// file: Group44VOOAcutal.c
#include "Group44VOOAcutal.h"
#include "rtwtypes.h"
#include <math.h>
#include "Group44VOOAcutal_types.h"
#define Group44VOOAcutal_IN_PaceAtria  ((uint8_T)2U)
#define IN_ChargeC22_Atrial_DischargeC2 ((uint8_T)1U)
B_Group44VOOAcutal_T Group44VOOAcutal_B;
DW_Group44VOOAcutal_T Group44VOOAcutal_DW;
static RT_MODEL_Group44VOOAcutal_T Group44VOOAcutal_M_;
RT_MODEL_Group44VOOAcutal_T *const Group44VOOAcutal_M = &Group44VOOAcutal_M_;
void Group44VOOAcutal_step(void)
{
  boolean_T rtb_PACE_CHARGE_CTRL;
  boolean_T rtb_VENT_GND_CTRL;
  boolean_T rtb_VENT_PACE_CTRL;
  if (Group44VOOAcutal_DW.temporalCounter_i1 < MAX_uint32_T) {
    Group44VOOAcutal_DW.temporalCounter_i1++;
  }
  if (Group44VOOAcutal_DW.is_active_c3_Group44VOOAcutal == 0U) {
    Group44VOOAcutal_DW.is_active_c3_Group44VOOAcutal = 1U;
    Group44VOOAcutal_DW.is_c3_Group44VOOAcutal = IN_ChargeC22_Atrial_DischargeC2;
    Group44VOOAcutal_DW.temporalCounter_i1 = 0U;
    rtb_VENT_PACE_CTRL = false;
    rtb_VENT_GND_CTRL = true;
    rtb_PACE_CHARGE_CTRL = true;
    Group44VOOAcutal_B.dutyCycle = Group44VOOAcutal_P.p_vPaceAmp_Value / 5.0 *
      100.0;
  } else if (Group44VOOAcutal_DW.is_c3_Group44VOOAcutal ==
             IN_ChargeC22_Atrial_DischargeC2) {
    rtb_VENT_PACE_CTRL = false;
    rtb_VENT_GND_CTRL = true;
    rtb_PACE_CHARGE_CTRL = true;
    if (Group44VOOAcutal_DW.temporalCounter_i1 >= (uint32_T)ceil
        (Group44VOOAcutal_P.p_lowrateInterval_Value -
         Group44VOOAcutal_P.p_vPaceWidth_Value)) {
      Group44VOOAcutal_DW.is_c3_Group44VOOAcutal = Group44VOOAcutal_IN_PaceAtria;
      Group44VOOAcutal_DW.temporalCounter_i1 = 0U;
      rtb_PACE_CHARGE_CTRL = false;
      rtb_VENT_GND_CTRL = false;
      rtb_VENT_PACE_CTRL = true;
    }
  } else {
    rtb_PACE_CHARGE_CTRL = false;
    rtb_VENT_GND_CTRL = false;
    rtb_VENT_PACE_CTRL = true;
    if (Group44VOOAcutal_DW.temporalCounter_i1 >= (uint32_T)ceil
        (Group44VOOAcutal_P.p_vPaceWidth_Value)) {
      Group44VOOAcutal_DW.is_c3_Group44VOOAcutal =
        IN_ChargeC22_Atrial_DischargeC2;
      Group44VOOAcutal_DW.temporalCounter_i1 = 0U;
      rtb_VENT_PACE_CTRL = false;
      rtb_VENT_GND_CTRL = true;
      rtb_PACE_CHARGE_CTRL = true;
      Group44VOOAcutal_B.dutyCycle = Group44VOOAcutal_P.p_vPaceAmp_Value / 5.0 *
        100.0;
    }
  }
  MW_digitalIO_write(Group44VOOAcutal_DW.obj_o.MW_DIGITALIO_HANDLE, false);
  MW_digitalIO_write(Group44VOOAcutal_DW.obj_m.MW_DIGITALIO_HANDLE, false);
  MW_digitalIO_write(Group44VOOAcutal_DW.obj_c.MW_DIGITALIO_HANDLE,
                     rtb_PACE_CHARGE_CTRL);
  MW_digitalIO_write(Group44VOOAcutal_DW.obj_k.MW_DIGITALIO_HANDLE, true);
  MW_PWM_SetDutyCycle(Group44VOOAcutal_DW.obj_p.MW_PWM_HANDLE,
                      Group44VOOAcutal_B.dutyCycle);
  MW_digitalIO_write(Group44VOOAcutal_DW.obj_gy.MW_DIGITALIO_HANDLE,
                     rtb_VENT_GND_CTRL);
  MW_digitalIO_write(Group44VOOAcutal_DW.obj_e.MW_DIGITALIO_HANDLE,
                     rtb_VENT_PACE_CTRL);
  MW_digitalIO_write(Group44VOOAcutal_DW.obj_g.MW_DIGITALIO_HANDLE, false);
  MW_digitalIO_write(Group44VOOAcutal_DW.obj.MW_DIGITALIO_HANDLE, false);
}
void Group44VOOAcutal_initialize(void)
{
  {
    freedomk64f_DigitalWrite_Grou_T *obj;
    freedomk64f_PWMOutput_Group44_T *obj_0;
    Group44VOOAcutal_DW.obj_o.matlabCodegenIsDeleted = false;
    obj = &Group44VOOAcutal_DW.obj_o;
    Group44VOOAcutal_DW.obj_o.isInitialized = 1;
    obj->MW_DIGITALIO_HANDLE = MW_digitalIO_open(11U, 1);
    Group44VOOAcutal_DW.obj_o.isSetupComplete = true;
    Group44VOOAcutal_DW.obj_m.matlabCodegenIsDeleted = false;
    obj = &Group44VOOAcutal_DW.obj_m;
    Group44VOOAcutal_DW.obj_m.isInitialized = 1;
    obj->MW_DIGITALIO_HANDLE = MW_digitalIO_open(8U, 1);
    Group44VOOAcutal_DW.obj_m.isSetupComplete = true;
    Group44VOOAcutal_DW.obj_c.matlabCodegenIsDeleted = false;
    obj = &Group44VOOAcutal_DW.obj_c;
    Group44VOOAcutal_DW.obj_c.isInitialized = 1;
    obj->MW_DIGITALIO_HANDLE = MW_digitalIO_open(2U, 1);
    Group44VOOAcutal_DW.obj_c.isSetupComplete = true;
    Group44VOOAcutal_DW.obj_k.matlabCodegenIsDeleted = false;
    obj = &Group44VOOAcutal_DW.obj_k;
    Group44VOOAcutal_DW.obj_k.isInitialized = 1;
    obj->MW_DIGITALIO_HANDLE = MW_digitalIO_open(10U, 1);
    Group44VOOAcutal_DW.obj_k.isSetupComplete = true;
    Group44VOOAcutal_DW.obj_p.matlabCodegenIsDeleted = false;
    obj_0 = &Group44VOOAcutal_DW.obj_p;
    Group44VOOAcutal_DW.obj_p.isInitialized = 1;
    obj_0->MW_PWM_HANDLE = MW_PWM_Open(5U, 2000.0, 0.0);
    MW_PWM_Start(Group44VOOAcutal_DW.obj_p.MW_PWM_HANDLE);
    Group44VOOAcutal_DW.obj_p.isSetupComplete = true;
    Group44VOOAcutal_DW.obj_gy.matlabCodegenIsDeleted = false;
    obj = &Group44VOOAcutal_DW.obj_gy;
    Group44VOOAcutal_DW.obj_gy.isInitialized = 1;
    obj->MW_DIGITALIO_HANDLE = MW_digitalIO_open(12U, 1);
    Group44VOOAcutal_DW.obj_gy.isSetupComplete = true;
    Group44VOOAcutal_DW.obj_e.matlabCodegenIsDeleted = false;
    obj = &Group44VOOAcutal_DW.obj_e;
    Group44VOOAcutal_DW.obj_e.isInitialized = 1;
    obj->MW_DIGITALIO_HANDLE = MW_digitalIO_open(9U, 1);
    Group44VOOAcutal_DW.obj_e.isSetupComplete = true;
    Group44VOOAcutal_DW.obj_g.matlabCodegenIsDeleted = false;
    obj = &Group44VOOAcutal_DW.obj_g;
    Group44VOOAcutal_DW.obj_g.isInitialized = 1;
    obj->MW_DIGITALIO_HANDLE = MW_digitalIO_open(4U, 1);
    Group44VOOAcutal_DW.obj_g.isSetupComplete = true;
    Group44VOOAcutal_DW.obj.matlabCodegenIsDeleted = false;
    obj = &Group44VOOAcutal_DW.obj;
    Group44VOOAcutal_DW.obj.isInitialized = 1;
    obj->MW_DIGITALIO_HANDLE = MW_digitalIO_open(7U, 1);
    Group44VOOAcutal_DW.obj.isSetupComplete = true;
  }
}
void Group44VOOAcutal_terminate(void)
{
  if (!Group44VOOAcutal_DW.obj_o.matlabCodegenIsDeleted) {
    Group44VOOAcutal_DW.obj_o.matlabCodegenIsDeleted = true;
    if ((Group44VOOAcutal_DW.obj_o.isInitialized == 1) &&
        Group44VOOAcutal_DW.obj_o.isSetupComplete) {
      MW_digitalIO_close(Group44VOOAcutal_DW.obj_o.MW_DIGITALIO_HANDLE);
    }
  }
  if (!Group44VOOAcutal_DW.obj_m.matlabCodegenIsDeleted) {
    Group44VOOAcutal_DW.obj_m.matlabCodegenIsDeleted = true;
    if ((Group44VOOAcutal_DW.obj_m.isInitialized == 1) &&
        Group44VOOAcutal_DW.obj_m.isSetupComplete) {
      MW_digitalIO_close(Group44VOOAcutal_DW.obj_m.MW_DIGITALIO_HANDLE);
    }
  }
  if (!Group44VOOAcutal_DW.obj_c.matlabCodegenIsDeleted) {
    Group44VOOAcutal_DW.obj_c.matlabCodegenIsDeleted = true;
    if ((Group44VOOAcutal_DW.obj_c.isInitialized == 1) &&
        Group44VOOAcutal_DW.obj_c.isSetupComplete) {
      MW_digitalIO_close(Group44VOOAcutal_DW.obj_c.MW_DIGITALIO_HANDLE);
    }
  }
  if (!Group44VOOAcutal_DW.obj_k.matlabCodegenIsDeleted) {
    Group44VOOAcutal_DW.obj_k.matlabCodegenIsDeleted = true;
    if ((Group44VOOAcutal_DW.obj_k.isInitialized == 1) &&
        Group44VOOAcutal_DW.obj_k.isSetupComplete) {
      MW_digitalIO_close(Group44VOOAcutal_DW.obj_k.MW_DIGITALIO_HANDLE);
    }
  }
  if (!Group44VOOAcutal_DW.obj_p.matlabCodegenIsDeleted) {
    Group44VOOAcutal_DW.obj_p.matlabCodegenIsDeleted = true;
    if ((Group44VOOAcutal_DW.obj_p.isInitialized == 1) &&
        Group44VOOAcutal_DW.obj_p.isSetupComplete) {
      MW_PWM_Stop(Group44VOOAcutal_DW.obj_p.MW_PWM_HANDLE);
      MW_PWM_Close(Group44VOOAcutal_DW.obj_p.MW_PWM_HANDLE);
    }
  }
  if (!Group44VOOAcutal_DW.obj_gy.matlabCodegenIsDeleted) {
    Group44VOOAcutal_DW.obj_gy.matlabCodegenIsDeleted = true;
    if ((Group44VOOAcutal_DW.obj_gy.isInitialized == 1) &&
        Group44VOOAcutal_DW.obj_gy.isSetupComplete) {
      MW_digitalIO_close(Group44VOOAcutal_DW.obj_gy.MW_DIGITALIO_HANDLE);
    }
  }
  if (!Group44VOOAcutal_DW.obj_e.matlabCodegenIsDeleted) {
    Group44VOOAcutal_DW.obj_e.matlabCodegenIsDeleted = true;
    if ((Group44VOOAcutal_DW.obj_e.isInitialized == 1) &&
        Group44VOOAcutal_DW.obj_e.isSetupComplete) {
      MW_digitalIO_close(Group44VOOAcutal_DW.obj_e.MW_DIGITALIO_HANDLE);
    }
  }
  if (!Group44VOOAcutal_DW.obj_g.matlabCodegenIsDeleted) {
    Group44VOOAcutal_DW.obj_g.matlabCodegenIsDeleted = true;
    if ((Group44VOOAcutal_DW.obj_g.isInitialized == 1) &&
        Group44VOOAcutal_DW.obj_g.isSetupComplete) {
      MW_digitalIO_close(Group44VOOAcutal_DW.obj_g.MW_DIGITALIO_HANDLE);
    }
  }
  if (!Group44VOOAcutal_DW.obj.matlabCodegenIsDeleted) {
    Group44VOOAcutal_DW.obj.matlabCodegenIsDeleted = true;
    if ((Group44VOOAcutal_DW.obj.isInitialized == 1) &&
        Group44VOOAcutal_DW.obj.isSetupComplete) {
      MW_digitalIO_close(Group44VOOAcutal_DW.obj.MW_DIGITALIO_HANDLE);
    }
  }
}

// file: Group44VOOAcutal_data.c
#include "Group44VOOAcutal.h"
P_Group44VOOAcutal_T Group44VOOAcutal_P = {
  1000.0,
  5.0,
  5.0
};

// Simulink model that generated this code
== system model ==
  DigitalWrite#1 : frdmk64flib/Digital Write  <- 1: Stateflowchart#1/7
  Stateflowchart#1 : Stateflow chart  <- 1: p_lowrateInterval, 2: p_vPaceWidth, 3: p_vPaceAmp
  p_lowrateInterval : Constant  Value=1000
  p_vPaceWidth : Constant  Value=5
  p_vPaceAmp : Constant  Value=5
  DigitalWrite#2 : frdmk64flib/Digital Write  <- 1: Stateflowchart#1/8
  PACE_CHARGE_CTRL : frdmk64flib/Digital Write  <- 1: Stateflowchart#1
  DigitalWrite#3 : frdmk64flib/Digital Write  <- 1: Stateflowchart#1/2
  PWMOutput#1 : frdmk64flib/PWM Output  <- 1: Stateflowchart#1/6
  VENT_GND_CTRL : frdmk64flib/Digital Write  <- 1: Stateflowchart#1/3
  VENT_PACE_CTRL : frdmk64flib/Digital Write  <- 1: Stateflowchart#1/4
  DigitalWrite#4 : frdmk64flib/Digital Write  <- 1: Stateflowchart#1/9
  DigitalWrite#5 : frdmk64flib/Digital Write  <- 1: Stateflowchart#1/5
== stateflow chart Stateflowchart#1 ==
  state ChargeC22_Atrial_DischargeC21
    entry:
    ATR_PACE_CTRL = false;
    VENT_PACE_CTRL = false;
    VENT_GND_CTRL = true;
    PACE_CHARGE_CTRL = true;
    PACE_GND_CTRL = true;
    Z_ATR_CTRL = false;
    Z_VENT_CTRL = false;
    ATR_GND_CTRL = false;
    dutyCycle=p_vPaceAmp/5.0*100
  state PaceAtria
    entry:
    PACE_CHARGE_CTRL = false;
    PACE_GND_CTRL = true;
    ATR_PACE_CTRL = false;
    ATR_GND_CTRL = false;
    Z_ATR_CTRL = false;
    Z_VENT_CTRL = false;
    VENT_GND_CTRL = false;
    VENT_PACE_CTRL = true;
    %natPaceDetected=false;
  (default) -> ChargeC22_Atrial_DischargeC21
  ChargeC22_Atrial_DischargeC21 -> PaceAtria : after(p_lowrateInterval-p_vPaceWidth,msec)
  PaceAtria -> ChargeC22_Atrial_DischargeC21 : after(p_vPaceWidth,msec)
  data: p_lowrateInterval input double; PACE_CHARGE_CTRL output boolean; PACE_GND_CTRL output boolean; VENT_GND_CTRL output boolean; VENT_PACE_CTRL output boolean; Z_VENT_CTRL output boolean; dutyCycle output double; p_vPaceWidth input double; p_vPaceAmp input double; ATR_GND_CTRL output; ATR_PACE_CTRL output; Z_ATR_CTRL output
